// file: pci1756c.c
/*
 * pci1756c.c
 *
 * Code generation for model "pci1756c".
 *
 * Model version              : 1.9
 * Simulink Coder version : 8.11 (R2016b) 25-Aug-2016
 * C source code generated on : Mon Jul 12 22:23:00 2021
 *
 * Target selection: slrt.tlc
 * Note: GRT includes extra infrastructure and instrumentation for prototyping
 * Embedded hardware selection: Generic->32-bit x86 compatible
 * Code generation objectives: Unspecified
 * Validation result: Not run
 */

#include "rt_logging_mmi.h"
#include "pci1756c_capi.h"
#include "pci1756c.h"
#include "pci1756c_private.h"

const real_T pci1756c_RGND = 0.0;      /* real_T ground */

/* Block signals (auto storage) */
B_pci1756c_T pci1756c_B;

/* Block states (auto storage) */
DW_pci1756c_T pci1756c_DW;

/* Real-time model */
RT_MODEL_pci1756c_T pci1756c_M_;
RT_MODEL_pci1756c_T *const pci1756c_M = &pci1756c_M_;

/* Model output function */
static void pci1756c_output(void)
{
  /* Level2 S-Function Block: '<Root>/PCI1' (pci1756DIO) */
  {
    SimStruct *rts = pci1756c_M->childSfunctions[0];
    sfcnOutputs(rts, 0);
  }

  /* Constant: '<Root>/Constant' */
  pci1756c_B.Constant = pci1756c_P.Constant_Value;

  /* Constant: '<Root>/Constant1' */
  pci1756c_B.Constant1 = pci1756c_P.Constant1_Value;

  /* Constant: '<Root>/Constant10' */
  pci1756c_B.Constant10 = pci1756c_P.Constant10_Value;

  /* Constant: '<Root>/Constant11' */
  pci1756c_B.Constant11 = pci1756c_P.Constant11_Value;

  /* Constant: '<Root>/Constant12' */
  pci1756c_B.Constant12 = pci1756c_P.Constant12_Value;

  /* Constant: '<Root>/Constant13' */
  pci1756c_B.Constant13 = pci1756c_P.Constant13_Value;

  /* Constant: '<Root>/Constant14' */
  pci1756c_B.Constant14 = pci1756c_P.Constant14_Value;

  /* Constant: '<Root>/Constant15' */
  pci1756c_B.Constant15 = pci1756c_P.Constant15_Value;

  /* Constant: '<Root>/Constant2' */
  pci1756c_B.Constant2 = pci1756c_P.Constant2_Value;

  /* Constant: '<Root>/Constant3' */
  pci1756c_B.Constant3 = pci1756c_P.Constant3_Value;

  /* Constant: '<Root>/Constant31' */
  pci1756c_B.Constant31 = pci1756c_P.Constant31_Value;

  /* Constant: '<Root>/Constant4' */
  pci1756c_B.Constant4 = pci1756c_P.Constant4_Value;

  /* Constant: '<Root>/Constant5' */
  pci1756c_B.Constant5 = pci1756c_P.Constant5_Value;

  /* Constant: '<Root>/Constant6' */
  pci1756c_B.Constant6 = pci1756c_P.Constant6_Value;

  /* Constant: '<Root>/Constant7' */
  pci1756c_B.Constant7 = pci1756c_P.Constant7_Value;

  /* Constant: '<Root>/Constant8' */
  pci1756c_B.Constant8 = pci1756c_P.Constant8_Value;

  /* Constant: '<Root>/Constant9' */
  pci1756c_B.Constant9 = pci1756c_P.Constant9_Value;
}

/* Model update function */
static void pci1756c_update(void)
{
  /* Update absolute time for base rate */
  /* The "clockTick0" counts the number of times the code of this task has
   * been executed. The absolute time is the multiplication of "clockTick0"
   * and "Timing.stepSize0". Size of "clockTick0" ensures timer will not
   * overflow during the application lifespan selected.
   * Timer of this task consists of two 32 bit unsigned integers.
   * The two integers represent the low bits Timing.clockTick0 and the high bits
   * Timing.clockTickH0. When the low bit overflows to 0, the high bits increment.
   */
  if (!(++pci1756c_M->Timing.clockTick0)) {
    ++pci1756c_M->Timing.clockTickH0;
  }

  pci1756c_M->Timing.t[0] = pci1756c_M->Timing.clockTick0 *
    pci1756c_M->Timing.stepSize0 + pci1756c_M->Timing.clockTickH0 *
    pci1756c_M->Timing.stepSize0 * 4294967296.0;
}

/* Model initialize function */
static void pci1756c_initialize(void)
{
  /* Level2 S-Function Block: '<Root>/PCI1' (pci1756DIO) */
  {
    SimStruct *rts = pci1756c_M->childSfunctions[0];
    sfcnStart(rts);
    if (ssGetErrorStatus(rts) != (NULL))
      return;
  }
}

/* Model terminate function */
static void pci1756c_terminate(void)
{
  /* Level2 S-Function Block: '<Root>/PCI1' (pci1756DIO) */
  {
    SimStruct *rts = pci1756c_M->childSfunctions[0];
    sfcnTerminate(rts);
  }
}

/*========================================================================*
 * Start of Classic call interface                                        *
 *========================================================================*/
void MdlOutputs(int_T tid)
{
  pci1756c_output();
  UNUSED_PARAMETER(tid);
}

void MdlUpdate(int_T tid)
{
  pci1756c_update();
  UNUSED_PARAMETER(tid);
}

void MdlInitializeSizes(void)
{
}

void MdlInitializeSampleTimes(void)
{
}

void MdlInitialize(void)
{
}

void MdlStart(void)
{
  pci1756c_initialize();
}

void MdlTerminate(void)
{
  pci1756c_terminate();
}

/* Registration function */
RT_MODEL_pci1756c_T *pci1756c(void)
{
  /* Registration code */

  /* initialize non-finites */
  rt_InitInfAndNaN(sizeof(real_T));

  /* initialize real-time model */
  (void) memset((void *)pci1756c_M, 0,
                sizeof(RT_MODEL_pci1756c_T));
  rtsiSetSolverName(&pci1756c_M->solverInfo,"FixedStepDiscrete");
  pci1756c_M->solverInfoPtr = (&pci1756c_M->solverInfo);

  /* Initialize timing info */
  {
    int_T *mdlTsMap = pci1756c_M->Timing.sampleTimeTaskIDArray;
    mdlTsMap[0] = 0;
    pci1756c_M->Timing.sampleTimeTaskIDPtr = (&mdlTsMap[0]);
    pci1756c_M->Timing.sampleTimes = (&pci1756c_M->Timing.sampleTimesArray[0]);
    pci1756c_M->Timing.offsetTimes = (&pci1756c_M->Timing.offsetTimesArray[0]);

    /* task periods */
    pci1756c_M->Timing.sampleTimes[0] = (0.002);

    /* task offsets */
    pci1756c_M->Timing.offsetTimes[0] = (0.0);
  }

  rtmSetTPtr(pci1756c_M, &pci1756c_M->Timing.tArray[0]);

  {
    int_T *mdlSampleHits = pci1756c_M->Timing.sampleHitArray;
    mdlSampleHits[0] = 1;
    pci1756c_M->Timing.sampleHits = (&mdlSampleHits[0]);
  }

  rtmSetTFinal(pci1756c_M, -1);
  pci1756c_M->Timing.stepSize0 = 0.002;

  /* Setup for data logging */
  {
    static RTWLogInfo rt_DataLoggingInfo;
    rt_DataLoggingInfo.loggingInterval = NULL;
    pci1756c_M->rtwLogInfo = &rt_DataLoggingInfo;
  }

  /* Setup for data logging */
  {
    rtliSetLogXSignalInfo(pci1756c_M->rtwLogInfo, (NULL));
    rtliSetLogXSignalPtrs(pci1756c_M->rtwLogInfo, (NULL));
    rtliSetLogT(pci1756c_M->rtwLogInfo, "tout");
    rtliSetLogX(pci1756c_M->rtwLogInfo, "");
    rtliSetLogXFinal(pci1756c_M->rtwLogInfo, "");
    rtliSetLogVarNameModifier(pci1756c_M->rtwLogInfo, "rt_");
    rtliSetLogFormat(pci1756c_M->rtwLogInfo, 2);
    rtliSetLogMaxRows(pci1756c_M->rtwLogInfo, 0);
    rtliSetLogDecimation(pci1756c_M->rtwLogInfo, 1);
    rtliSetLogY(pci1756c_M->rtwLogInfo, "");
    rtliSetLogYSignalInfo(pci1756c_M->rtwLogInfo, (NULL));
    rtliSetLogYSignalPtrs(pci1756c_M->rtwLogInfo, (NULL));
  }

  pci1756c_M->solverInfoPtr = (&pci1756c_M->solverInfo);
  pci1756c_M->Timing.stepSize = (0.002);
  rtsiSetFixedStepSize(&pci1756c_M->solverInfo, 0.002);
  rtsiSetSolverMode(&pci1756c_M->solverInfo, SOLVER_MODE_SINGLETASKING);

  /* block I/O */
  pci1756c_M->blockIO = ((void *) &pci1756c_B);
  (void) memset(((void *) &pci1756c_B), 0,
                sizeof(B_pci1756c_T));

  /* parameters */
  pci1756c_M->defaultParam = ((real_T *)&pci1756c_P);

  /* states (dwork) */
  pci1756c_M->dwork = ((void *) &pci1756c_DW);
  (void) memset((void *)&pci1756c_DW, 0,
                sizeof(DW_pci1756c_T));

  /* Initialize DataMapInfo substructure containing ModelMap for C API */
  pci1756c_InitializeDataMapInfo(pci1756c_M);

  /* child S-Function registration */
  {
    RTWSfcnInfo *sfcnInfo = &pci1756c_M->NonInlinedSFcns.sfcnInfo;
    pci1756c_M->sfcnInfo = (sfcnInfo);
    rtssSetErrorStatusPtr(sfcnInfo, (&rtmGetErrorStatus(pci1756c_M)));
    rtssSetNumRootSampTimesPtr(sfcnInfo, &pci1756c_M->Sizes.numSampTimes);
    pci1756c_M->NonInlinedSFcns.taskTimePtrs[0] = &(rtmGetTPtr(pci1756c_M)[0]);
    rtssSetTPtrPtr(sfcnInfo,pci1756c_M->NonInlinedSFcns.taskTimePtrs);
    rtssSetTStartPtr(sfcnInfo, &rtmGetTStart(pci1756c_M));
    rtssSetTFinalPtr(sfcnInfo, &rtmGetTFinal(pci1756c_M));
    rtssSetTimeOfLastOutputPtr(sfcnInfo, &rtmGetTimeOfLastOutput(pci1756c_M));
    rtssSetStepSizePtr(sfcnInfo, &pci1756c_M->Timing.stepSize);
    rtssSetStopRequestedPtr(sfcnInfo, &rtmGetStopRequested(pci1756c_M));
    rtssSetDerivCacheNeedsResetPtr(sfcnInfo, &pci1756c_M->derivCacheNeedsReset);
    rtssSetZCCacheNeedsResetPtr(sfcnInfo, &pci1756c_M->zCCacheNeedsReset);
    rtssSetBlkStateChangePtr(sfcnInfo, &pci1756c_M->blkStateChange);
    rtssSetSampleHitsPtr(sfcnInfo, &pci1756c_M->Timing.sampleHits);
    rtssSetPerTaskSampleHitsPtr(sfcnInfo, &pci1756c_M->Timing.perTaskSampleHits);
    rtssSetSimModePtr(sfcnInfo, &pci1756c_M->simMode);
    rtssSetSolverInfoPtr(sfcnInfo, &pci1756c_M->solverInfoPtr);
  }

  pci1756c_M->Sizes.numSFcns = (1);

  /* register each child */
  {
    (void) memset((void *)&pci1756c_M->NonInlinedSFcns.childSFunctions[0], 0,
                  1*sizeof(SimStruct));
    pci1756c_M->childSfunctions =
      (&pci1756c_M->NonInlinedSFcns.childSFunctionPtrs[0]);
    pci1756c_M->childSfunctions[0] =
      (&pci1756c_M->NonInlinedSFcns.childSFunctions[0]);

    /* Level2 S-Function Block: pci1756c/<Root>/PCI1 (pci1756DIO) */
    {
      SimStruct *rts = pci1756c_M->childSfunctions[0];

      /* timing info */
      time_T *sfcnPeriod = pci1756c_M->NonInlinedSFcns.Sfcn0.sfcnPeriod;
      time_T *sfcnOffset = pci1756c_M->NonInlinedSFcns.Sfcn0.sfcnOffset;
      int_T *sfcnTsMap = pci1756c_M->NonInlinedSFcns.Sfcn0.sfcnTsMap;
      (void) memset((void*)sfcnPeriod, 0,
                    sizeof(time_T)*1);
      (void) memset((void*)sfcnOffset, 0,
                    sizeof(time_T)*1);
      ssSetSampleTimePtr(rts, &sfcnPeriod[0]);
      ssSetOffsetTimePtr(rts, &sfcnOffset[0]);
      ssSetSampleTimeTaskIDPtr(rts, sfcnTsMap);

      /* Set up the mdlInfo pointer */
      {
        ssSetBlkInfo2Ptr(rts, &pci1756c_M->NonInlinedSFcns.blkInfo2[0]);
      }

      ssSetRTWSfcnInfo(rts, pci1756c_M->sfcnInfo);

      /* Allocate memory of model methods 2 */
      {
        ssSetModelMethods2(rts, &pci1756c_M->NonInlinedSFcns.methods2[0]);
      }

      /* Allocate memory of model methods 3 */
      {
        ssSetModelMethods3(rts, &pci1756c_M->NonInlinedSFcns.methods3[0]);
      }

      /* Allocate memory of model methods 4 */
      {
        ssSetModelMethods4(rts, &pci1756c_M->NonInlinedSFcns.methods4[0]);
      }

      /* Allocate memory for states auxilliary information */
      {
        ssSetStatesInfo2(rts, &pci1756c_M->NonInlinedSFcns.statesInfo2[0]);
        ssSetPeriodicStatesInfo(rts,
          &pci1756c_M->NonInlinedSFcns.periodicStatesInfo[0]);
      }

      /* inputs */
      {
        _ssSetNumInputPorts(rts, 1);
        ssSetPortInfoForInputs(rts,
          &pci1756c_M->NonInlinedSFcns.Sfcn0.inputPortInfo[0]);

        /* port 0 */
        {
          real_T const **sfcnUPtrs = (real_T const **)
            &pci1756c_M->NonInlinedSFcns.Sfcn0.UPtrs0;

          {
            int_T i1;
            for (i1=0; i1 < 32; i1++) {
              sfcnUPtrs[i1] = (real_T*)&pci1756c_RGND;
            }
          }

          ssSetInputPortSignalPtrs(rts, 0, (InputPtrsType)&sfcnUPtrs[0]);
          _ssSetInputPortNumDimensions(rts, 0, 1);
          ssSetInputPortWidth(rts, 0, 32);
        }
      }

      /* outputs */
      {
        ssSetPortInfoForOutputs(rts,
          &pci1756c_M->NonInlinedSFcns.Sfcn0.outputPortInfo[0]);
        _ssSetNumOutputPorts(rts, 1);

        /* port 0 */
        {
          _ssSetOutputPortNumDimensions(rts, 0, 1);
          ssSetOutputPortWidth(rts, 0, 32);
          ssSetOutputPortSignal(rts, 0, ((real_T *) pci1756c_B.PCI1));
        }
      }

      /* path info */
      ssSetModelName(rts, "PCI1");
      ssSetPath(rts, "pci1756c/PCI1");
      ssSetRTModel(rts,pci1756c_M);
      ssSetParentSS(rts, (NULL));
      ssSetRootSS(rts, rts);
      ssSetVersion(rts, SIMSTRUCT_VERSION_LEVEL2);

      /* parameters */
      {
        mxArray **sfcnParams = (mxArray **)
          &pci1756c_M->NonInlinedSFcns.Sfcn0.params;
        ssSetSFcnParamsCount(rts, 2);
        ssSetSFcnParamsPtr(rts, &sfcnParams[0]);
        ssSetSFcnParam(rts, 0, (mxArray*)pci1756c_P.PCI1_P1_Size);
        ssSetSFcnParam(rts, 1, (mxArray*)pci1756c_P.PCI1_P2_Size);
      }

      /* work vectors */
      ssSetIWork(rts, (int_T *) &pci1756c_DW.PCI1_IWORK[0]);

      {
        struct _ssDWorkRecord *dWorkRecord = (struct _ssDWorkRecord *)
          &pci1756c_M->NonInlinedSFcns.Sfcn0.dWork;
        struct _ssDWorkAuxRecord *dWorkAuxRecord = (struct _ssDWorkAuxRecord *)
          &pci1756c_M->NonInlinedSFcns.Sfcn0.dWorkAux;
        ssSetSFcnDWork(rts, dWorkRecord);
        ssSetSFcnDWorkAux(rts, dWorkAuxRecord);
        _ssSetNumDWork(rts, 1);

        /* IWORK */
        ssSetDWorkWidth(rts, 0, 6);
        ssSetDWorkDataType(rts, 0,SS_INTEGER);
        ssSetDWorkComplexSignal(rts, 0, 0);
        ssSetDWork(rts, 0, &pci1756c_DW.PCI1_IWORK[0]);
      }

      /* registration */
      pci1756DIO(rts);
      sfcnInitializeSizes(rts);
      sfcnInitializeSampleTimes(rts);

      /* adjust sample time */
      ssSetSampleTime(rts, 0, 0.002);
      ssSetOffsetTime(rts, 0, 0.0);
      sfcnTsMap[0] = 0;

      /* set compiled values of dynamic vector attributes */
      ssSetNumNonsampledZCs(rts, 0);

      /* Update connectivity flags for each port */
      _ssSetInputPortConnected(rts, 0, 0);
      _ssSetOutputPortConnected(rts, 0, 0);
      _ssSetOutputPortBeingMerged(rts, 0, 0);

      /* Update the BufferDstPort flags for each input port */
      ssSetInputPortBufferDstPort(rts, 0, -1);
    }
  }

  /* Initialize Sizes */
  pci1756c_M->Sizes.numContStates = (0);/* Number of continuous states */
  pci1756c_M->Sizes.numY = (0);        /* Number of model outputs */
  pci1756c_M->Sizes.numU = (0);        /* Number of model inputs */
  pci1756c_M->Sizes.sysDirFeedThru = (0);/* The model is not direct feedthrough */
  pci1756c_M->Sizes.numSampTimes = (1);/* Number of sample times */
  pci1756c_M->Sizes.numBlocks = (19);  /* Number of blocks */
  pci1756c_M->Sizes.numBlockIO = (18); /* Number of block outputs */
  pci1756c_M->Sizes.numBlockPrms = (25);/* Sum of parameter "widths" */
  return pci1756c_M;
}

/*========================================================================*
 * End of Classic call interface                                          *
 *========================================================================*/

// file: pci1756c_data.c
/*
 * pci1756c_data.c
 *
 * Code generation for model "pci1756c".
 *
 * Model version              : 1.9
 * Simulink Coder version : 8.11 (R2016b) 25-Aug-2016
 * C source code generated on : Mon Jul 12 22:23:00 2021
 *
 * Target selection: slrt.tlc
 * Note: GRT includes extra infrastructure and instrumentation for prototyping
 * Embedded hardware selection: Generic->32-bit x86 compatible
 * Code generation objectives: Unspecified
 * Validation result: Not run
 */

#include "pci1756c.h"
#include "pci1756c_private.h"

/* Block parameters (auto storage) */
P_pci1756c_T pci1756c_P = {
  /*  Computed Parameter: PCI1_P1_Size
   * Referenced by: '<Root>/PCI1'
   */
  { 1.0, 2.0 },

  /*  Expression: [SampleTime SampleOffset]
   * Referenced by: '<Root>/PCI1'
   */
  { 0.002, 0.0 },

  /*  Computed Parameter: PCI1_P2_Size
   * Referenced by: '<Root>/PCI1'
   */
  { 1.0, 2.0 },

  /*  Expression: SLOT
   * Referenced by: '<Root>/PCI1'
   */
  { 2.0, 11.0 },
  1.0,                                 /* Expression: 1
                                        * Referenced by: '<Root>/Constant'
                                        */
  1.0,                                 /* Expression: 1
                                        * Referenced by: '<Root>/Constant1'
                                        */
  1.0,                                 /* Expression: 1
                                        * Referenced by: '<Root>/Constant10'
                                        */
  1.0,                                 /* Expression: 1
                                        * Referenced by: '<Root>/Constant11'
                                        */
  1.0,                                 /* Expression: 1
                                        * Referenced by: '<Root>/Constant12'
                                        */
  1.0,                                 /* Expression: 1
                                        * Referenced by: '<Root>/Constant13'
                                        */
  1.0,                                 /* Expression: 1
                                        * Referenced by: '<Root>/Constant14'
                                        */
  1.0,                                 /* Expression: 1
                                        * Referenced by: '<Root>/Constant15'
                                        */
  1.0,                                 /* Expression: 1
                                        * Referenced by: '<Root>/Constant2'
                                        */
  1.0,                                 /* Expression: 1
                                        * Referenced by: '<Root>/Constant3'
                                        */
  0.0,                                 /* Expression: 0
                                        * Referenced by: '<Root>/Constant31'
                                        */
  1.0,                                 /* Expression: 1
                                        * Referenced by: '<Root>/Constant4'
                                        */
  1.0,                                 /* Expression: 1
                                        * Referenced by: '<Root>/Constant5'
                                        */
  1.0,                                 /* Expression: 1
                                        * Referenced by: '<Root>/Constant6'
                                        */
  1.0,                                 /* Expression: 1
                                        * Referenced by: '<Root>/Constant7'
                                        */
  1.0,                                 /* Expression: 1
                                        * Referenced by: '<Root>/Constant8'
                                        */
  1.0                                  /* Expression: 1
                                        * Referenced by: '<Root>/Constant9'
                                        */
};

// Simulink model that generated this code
simulink model "pci1756c"  (R2016b)
settings: Solver=ode4  StartTime=0.0  StopTime=inf  FixedStep=0.002  RelTol=1e-3  EnableMultiTasking=on

== system pci1756c ==
  note: 输出
  Constant{,1..15} (16 alike) : Constant
  Constant31 : Constant  Value=0
  Mux : Mux  Inputs=32
  PCI1 : S-Function  FunctionName=pci1756DIO  Parameters=[SampleTime SampleOffset], SLOT  SFunctionDeploymentMode=off  EnableBusSupport=off  mask(PCI1756){Sample=0.002, SLOT=[2 11]}
      mask prompts: Sample "Sample time:"
      mask help:
      | PCI-1756
      | Advantech
      | Digital Input&Output
      mask init:
      | SampleTime =0.002; SampleOffset=0;
  输入 : Display
  wires:
  Constant/1 -> Mux/1
  Constant1/1 -> Mux/2
  Constant2/1 -> Mux/3
  Constant3/1 -> Mux/4
  Constant4/1 -> Mux/5
  Constant5/1 -> Mux/6
  Constant6/1 -> Mux/7
  Constant7/1 -> Mux/8
  Constant8/1 -> Mux/9
  Constant9/1 -> Mux/10
  Constant10/1 -> Mux/11
  Constant11/1 -> Mux/12
  Constant12/1 -> Mux/13
  Constant13/1 -> Mux/14
  Constant14/1 -> Mux/15
  Constant15/1 -> Mux/16
  Constant31/1 -> Mux/32, Mux/31, Mux/30, Mux/29, Mux/28, Mux/27, Mux/26, Mux/25, Mux/24, Mux/23, Mux/22, Mux/21, Mux/20, Mux/19, Mux/17, Mux/18
  Mux/1 -> PCI1/1
  PCI1/1 -> 输入/1
